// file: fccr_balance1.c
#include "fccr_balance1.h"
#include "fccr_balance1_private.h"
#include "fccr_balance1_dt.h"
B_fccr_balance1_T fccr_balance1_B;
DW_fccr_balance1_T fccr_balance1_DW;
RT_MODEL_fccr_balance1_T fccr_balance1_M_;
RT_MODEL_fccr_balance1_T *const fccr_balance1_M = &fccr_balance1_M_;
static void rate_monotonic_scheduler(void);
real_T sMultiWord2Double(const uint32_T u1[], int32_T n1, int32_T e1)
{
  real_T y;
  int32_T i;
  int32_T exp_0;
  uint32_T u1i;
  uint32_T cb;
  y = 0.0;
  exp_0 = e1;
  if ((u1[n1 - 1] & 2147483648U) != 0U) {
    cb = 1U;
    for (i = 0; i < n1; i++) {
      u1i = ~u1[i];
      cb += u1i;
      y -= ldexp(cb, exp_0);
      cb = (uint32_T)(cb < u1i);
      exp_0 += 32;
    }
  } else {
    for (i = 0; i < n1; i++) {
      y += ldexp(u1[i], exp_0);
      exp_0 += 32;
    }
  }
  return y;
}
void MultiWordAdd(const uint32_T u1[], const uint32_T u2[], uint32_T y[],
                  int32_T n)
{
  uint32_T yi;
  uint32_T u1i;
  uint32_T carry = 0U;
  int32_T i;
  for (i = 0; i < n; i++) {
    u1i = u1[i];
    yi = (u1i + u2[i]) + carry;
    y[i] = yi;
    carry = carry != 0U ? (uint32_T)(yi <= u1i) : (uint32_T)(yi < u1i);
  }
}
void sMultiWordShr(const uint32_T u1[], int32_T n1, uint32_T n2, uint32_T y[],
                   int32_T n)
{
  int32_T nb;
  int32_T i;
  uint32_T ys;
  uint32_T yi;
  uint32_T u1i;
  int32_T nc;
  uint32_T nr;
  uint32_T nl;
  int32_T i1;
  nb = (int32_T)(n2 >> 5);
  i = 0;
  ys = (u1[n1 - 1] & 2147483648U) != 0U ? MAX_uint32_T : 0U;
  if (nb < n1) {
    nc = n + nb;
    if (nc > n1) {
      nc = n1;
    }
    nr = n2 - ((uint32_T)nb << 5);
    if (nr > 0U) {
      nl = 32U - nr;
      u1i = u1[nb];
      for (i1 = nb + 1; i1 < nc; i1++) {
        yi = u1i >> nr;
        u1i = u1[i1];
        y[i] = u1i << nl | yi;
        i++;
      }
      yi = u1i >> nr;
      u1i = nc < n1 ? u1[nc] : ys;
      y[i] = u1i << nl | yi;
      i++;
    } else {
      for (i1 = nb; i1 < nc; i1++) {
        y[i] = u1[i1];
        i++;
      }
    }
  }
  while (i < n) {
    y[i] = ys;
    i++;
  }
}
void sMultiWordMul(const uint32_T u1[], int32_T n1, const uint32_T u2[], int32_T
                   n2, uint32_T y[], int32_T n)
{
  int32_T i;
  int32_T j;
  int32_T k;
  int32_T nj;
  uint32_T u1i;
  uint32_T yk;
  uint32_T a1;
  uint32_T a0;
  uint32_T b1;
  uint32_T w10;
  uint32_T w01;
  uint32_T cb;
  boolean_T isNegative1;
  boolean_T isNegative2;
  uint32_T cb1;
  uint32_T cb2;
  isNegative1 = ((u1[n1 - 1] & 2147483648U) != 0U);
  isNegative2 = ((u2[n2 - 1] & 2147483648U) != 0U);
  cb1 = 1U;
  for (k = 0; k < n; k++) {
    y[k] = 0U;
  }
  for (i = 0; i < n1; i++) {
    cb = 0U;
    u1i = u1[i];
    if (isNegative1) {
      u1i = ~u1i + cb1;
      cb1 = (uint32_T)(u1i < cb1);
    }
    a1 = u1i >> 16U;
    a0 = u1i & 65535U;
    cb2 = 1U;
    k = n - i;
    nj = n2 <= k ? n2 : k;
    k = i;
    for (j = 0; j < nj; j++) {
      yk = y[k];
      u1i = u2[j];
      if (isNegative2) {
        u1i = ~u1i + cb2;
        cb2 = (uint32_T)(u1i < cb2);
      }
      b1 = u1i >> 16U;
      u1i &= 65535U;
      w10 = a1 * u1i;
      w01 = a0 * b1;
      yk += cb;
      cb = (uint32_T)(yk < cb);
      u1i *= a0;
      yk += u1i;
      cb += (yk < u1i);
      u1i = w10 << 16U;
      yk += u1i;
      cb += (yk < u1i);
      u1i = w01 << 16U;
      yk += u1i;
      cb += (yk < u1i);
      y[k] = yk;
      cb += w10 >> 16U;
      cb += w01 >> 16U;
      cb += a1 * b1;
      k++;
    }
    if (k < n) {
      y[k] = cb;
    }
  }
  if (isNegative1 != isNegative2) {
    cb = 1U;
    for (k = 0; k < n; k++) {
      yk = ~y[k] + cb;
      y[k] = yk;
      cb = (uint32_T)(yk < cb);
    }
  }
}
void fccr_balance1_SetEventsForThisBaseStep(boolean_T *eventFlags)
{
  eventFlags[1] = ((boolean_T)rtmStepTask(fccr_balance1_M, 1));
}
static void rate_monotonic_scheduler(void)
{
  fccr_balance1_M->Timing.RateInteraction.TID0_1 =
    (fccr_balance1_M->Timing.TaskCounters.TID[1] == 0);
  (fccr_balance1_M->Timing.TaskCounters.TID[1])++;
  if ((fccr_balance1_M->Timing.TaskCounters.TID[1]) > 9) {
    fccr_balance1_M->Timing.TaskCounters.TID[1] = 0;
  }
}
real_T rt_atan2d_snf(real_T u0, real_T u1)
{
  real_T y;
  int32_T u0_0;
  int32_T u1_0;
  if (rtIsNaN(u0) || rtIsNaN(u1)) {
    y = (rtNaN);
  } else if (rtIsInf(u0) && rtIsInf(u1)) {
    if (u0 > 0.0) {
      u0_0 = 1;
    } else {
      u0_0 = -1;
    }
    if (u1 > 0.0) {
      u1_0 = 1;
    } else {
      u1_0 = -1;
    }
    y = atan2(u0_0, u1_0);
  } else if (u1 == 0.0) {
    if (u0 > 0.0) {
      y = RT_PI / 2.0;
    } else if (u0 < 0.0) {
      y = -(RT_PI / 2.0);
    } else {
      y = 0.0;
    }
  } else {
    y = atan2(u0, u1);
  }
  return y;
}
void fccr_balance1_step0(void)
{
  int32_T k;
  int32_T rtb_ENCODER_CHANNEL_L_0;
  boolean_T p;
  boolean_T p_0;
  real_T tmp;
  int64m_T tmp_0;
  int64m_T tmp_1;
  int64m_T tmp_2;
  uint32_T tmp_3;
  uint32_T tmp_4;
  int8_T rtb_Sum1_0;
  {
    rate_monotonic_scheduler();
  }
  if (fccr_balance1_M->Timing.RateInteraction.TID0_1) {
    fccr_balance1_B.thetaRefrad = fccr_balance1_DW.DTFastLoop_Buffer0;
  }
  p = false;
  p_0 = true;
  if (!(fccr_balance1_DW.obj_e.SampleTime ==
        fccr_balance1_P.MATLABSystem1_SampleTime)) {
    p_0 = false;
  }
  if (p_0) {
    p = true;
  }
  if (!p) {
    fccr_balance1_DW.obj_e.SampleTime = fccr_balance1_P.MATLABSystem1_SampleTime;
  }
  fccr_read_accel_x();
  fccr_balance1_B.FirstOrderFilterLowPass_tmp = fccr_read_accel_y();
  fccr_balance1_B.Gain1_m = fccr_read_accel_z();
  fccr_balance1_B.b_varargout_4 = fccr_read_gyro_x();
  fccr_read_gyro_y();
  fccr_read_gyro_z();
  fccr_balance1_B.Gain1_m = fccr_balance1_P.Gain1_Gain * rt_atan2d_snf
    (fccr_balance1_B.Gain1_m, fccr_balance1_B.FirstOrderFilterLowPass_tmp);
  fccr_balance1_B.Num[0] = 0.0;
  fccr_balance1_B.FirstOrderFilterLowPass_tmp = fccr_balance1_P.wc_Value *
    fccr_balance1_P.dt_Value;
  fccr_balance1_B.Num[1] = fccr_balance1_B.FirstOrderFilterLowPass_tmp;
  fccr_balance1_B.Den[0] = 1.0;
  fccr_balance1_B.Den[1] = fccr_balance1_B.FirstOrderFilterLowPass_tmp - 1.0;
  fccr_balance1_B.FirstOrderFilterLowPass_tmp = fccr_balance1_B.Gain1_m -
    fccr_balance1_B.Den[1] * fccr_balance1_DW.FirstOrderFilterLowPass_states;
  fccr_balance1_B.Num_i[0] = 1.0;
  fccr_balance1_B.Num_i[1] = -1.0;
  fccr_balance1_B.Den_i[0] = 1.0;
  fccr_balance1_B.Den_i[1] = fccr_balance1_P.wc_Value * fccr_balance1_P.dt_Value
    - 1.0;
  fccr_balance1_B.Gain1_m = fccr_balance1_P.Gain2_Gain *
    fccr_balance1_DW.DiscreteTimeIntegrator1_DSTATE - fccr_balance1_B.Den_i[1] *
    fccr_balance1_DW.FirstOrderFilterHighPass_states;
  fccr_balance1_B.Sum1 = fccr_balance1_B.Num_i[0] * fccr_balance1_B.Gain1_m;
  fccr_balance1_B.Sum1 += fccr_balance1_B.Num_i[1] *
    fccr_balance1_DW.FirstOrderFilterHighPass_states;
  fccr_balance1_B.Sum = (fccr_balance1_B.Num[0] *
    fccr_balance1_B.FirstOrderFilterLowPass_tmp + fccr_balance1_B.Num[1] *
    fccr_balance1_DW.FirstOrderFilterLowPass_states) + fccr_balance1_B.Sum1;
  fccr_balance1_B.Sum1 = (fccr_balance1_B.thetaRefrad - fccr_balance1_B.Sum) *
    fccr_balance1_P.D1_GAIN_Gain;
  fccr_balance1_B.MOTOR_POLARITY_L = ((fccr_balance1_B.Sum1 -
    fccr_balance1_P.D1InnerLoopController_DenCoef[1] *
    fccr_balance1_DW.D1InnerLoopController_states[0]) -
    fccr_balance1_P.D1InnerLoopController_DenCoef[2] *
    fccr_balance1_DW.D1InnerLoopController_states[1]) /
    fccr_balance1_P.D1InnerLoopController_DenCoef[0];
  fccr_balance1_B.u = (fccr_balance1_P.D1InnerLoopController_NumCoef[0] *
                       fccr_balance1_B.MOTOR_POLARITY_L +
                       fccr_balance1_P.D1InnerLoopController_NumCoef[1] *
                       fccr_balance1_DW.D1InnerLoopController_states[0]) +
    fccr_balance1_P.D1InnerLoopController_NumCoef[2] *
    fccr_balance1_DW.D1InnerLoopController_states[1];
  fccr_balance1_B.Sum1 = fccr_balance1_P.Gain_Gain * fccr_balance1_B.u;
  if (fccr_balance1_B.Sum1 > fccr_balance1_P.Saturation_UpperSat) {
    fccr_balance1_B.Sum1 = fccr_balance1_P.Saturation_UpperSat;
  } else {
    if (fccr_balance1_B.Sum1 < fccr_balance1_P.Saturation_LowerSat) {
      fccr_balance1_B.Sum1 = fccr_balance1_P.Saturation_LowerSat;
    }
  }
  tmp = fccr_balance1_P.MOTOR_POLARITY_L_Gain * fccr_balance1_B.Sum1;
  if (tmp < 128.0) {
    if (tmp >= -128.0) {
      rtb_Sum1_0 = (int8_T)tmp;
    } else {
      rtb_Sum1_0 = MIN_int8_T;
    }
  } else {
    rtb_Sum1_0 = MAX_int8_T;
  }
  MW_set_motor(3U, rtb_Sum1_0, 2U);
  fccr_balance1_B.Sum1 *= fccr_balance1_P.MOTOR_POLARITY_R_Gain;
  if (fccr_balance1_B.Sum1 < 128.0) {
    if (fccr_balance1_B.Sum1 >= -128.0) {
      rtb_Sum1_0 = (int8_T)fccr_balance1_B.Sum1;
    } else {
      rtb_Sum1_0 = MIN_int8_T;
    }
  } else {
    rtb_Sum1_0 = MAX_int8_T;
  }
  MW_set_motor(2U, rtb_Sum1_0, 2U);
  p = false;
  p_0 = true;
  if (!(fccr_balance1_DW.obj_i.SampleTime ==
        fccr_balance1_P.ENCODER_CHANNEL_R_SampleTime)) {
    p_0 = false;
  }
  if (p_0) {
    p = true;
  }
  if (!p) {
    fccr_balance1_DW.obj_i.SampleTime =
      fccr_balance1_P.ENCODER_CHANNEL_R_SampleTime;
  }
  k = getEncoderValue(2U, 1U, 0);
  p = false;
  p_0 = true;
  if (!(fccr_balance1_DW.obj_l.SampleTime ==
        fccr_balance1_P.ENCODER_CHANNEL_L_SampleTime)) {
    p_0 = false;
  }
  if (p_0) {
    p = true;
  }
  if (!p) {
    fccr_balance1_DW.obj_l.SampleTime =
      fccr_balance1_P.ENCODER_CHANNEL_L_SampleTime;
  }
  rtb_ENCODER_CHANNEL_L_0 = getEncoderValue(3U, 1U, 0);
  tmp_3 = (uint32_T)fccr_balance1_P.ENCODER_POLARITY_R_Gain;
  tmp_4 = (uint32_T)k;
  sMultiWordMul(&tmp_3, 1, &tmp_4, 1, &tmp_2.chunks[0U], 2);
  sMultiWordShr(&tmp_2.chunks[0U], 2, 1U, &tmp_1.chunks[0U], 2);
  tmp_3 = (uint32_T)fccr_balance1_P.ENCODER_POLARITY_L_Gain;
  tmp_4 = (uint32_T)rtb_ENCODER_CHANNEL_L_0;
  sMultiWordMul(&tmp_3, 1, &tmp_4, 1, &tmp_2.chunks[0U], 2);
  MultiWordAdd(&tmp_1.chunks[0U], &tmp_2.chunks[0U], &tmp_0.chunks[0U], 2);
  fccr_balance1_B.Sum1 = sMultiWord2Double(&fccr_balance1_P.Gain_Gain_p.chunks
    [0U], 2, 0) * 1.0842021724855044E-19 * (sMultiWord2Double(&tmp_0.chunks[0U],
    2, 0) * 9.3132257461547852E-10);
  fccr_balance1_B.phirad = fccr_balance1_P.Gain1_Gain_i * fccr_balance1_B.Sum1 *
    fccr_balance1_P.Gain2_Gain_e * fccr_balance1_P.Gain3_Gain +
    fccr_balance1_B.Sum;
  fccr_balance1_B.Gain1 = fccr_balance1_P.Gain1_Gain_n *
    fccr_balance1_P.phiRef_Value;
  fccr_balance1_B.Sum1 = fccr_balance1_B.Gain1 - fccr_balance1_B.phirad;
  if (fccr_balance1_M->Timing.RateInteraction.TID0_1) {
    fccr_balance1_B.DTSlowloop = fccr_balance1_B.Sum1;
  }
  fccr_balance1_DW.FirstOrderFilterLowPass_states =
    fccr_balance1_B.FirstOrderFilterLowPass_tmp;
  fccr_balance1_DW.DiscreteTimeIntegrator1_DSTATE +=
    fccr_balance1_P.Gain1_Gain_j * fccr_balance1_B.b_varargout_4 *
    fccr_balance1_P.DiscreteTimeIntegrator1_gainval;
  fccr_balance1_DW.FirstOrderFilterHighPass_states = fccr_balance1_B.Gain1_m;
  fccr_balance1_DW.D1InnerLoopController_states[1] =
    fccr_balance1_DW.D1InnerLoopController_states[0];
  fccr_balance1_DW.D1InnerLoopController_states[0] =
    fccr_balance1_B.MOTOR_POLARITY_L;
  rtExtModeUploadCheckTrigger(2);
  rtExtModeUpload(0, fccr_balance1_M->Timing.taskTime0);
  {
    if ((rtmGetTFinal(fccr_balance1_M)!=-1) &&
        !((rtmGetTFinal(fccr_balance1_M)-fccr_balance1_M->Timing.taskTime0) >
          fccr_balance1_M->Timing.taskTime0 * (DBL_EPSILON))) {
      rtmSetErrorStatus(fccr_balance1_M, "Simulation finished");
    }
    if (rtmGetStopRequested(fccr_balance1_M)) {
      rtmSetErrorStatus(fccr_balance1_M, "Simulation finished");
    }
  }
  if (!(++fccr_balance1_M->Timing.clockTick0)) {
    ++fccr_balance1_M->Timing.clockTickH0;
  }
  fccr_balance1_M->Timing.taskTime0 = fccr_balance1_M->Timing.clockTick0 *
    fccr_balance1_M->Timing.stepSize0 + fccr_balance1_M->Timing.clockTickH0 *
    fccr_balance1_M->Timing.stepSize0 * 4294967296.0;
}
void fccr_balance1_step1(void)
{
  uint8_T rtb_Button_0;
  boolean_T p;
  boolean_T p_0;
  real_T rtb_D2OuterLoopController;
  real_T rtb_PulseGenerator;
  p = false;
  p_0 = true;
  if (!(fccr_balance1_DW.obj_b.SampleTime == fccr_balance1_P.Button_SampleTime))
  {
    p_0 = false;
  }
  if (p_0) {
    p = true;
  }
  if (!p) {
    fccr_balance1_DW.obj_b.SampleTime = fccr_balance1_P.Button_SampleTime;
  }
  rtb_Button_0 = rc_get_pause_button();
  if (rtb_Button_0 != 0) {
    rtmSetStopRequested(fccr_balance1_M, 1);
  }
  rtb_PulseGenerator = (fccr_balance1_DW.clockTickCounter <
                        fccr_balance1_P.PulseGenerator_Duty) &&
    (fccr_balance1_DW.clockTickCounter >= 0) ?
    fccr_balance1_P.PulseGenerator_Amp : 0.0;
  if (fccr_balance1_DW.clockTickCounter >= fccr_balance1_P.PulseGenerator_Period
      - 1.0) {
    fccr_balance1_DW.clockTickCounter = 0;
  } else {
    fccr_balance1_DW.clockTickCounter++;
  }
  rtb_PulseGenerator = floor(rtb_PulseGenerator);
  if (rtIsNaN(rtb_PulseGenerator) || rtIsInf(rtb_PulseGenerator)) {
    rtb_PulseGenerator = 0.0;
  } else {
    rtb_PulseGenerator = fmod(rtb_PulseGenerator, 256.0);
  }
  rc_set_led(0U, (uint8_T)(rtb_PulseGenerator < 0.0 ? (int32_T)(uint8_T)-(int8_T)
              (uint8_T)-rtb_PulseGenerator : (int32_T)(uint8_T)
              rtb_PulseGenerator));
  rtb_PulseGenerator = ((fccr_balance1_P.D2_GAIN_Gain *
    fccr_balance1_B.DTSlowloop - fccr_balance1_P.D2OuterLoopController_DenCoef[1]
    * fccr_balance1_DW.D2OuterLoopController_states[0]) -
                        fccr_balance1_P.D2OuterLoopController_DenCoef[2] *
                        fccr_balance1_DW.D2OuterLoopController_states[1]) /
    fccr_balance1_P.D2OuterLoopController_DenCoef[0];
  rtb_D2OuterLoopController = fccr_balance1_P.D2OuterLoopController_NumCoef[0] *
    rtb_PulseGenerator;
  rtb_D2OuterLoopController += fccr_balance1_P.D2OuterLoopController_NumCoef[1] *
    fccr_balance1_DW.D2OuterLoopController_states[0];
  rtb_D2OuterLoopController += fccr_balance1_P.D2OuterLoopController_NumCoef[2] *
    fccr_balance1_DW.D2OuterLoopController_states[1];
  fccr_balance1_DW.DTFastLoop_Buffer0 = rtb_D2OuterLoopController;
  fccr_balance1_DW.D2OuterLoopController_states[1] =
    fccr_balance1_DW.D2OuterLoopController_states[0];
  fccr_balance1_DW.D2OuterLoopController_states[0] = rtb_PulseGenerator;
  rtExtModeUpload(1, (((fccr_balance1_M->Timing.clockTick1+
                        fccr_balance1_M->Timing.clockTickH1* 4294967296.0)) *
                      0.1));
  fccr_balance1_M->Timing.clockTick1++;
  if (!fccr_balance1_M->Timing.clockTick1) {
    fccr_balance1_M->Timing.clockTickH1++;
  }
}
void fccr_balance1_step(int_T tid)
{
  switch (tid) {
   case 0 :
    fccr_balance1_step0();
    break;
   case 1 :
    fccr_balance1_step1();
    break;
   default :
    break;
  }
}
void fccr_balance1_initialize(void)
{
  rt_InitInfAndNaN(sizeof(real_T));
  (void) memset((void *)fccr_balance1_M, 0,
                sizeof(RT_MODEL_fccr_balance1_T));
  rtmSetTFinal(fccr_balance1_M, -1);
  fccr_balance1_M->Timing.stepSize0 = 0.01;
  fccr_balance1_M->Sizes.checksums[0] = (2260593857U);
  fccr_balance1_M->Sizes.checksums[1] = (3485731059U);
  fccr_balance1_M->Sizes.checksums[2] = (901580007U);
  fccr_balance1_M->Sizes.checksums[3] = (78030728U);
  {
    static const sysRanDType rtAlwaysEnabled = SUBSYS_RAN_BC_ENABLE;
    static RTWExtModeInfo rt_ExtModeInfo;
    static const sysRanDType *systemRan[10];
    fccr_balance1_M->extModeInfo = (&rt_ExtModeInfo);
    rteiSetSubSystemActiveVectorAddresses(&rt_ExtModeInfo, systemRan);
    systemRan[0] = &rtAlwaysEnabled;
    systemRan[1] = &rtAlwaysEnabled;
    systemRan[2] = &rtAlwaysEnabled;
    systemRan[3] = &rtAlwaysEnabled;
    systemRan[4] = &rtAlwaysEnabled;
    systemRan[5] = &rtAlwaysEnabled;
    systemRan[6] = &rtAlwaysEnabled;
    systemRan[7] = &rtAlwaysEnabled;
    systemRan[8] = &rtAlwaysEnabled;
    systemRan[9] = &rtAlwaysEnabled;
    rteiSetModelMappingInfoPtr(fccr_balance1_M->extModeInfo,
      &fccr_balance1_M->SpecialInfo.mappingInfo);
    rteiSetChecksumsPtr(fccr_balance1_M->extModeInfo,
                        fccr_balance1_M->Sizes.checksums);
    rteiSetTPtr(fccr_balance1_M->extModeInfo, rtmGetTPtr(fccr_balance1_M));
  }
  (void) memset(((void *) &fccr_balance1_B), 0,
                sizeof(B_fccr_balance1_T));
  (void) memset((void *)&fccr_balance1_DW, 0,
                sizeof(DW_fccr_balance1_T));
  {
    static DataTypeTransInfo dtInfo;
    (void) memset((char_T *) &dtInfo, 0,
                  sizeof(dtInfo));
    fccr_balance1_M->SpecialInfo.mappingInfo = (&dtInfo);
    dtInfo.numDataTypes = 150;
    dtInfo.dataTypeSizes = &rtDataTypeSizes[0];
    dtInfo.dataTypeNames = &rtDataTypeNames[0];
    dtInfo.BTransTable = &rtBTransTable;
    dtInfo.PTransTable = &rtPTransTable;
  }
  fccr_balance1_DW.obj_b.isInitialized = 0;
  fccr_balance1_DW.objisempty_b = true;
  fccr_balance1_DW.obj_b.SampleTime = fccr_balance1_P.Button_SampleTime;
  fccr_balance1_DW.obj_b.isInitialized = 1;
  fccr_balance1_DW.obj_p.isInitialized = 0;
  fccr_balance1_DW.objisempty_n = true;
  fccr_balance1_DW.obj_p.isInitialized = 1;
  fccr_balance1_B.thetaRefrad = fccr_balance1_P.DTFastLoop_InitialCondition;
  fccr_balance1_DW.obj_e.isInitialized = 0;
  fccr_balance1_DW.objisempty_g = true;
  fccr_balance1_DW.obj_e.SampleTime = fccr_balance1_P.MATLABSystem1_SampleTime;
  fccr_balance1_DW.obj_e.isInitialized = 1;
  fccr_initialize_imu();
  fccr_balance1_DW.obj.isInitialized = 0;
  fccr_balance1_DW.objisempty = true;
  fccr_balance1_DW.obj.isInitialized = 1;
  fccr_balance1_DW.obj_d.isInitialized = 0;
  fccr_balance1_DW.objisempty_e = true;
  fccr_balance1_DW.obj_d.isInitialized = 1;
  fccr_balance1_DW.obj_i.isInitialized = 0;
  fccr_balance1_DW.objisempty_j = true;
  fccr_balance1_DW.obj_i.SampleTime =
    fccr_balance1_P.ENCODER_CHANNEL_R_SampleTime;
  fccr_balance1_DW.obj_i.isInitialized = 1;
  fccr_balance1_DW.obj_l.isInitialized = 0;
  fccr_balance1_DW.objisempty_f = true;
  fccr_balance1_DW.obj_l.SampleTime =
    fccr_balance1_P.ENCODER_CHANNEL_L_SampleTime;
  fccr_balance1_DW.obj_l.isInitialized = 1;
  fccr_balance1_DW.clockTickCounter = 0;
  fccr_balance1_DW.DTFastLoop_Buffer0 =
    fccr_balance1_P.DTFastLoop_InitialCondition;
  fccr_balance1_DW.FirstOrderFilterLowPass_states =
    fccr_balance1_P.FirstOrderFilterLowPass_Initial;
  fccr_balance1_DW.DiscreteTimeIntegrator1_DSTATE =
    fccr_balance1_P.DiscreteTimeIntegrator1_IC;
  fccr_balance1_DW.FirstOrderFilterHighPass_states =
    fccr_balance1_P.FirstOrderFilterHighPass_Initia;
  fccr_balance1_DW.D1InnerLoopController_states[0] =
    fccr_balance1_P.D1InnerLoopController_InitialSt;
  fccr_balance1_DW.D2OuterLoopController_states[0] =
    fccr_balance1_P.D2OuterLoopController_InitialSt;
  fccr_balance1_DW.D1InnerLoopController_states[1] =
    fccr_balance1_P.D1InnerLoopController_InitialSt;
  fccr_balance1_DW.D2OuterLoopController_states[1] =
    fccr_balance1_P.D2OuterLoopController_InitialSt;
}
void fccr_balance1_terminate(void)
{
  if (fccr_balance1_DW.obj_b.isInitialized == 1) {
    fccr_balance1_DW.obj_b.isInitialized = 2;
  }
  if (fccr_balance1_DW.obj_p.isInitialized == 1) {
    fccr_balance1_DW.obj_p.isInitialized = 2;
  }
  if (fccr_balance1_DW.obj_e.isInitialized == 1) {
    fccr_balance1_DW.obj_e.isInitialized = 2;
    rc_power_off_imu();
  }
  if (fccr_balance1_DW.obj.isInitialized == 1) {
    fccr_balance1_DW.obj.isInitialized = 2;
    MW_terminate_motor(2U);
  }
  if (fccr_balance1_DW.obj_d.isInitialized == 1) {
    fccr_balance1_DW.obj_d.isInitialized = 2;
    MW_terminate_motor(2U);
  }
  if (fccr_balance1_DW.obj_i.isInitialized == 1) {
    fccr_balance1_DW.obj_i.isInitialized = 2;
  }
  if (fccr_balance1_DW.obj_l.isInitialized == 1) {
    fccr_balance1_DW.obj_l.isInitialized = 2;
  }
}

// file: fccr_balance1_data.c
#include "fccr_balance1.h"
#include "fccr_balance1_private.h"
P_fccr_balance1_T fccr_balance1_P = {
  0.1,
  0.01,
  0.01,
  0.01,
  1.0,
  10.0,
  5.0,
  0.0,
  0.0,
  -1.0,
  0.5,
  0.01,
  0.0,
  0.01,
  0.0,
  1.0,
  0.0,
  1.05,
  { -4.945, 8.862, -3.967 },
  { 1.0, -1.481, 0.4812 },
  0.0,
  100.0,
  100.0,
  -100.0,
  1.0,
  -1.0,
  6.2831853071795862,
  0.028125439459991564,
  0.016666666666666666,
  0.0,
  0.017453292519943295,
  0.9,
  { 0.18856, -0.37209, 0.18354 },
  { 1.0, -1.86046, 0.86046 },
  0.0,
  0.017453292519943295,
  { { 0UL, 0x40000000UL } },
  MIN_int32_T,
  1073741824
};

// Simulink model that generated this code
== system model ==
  DCMotor#1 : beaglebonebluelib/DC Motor  <- 1: DataTypeConversion#1
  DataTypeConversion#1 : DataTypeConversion  <- 1: MOTOR_POLARITY_L
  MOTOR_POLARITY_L : Gain  <- 1: Saturation
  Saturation : Saturate  UpperLimit=100  LowerLimit=-100  <- 1: Gain
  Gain : Gain  Gain=100  <- 1: D1InnerLoopController
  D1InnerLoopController : DiscreteTransferFcn  Numerator=[-4.945, 8.862, -3.967]  Denominator=[1.000, -1.481, 0.4812]  <- 1: D1_GAIN
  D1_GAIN : Gain  Gain=1.05  <- 1: Sum
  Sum : Sum  Inputs=+-  <- 1: DTFastLoop, 2: Sum#1
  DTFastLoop : RateTransition  <- 1: D2OuterLoopController
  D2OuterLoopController : DiscreteTransferFcn  Numerator="[0.18856,  -0.37209,  0.18354]"  Denominator="[1.00000,  -1.86046,   0.86046]"  <- 1: D2_GAIN
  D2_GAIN : Gain  Gain=0.9  <- 1: DTSlowloop
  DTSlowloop : RateTransition  <- 1: Sum1
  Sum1 : Sum  Inputs=+-  <- 1: DegreestoRadians#1, 2: Sum#2
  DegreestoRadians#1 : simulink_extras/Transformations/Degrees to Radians  <- 1: phiRef
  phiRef : Constant  Value=0
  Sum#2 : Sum  Inputs=++  <- 1: Sum#1, 2: Gain3
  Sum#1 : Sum  Inputs=++  <- 1: FirstOrderFilterLowPass, 2: FirstOrderFilterHighPass
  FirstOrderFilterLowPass : DiscreteTransferFcn  Denominator=[1]  <- 1: Gain1, 2: MATLABFunction#1, 3: MATLABFunction#1/2
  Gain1 : Gain  Gain=-1  <- 1: Trigonometry#1
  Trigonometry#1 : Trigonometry  Operator=atan2  <- 1: MATLABSystem1/3, 2: MATLABSystem1/2
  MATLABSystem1 : MATLABSystem
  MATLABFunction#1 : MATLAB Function  <- 1: wc, 2: dt
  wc : Constant  Value=0.5
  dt : Constant  Value=0.01
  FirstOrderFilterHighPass : DiscreteTransferFcn  Denominator=[1]  <- 1: Gain2, 2: MATLABFunction#2, 3: MATLABFunction#2/2
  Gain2 : Gain  <- 1: DiscreteTimeIntegrator1
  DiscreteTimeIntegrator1 : DiscreteIntegrator  <- 1: DegreestoRadians#2
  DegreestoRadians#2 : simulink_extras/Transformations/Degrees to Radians  <- 1: MATLABSystem1/4
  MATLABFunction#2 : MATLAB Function  <- 1: wc, 2: dt
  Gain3 : Gain  Gain=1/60  <- 1: Gain#1
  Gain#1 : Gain  Gain=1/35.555  <- 1: Gain#2
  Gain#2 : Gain  Gain=2*pi  <- 1: Gain#3
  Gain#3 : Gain  Gain=0.5  <- 1: Sum#3
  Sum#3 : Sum  Inputs=++  <- 1: ENCODER_POLARITY_R, 2: ENCODER_POLARITY_L
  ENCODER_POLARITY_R : Gain  Gain=-1  <- 1: ENCODER_CHANNEL_R
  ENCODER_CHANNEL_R : beaglebonebluelib/Encoder
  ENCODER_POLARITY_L : Gain  <- 1: ENCODER_CHANNEL_L
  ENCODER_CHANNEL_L : beaglebonebluelib/Encoder
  DCMotor#2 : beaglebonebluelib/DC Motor  <- 1: DataTypeConversion#2
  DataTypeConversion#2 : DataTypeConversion  <- 1: MOTOR_POLARITY_R
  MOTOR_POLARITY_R : Gain  Gain=-1  <- 1: Saturation
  Stop#1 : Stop  <- 1: DataTypeConversion#3
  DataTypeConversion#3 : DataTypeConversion  <- 1: Button
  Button : beaglebonebluelib/Button
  LED#1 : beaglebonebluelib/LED  <- 1: DataTypeConversion#4
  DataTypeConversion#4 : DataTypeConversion  <- 1: PulseGenerator
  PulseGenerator : DiscretePulseGenerator  Period=10  PulseWidth=5

